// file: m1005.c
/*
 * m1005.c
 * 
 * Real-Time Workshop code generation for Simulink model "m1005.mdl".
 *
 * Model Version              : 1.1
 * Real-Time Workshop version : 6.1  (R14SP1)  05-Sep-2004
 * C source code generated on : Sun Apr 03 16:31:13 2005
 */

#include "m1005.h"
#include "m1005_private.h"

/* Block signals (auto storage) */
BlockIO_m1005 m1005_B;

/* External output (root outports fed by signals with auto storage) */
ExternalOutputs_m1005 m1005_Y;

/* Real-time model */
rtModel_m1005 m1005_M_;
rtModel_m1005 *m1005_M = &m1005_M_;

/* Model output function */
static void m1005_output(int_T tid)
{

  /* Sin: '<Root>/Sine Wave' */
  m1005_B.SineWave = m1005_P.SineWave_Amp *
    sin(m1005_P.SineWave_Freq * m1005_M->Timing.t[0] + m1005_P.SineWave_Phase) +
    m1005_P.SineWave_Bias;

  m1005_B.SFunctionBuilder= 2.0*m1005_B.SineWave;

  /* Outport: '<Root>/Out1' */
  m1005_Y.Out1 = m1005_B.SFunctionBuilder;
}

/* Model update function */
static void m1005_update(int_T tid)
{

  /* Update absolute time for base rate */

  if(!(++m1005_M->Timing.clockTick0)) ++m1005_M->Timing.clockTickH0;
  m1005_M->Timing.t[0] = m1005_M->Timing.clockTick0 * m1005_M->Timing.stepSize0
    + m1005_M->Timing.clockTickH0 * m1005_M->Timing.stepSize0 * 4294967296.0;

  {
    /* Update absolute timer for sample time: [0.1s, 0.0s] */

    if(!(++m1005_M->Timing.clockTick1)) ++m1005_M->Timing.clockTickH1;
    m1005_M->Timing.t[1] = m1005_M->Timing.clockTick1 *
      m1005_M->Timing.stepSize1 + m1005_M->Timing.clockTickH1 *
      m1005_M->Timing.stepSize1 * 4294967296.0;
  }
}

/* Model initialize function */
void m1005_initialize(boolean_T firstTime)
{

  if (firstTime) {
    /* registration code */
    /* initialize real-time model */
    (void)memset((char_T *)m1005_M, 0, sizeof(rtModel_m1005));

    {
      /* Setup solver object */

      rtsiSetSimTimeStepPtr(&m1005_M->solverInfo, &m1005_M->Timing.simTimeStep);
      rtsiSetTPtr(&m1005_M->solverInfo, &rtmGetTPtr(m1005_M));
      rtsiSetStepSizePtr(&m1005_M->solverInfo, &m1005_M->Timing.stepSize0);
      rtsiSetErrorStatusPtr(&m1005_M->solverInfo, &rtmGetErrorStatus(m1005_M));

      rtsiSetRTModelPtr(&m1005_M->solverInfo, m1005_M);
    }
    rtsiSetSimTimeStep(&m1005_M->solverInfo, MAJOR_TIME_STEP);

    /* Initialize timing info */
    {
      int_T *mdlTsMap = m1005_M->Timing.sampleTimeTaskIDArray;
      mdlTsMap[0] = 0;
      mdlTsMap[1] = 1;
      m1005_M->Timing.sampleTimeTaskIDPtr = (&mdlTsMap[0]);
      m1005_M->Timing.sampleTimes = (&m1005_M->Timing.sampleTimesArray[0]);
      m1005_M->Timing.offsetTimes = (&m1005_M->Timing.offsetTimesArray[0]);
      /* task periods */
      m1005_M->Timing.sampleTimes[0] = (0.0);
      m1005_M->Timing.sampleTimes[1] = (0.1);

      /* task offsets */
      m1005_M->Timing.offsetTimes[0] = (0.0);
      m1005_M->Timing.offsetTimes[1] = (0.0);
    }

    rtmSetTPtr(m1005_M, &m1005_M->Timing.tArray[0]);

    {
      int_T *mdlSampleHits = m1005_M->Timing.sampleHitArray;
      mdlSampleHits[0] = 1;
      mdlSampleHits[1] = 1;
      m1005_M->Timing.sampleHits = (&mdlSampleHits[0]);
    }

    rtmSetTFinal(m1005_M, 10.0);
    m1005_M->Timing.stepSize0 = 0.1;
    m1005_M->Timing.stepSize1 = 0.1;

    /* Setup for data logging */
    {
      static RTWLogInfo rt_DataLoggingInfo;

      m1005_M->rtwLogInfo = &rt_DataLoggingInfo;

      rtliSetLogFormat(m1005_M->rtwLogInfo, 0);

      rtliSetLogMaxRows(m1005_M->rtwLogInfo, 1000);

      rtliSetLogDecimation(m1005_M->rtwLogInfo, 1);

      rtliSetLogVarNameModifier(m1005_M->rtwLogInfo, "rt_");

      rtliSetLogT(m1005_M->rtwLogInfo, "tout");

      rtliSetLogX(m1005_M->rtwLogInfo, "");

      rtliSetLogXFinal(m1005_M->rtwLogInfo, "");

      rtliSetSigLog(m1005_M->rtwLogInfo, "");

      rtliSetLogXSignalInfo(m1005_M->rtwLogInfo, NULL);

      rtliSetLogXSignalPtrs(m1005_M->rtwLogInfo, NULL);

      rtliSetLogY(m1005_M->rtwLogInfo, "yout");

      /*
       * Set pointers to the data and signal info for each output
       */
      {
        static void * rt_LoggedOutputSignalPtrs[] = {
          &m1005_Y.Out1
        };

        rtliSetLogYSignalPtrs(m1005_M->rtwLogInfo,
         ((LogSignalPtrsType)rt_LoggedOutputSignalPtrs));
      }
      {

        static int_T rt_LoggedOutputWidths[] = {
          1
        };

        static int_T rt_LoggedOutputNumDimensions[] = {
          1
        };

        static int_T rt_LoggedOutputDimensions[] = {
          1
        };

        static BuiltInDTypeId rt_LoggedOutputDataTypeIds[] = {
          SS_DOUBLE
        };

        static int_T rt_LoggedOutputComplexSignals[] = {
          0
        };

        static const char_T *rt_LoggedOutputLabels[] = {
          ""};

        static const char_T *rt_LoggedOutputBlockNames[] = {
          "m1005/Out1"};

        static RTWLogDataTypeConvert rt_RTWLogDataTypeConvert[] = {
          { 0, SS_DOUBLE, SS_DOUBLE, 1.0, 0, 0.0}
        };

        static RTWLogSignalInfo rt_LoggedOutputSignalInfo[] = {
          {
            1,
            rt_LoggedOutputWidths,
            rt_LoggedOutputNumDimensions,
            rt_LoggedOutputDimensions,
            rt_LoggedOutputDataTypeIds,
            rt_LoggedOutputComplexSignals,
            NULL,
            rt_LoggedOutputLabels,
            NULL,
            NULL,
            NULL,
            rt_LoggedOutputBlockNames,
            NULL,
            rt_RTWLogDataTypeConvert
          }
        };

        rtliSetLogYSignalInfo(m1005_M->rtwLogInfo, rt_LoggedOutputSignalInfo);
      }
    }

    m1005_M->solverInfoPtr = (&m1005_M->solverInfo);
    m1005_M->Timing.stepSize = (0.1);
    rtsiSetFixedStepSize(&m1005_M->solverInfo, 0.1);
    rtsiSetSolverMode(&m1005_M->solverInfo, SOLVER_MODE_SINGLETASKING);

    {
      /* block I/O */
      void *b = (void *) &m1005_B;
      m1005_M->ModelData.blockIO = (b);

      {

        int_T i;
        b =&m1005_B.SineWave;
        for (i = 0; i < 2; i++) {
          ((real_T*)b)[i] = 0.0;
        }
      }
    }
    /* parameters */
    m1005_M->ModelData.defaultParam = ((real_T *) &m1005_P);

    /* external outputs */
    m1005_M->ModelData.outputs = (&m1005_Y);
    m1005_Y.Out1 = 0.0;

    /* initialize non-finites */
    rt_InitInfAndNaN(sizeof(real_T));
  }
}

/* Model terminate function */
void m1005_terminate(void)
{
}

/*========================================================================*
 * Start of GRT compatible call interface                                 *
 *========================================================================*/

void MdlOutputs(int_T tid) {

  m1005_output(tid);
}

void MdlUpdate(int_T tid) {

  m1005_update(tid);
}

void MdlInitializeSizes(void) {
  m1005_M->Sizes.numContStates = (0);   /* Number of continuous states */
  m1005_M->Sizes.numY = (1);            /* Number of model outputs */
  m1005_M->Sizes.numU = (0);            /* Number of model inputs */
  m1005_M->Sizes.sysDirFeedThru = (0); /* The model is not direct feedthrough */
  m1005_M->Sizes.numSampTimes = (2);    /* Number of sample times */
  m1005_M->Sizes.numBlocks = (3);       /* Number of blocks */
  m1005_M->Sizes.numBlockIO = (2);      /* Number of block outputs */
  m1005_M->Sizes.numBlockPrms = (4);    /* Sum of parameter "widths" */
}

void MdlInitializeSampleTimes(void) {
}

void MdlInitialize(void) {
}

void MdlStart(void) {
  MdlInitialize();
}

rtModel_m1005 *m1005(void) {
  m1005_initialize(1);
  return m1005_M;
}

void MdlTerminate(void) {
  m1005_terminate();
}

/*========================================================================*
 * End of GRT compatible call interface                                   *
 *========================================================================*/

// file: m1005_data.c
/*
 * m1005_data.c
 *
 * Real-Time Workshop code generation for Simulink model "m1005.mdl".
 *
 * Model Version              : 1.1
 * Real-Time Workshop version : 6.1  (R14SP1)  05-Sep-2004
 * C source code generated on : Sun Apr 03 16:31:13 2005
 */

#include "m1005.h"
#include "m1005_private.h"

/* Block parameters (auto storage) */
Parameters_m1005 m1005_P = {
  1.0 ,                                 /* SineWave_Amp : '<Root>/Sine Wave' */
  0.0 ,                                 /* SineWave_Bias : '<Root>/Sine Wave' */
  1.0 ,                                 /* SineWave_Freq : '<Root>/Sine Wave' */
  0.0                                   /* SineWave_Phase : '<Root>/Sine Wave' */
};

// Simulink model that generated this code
simulink model "m1005"  (Simulink 6.1)
settings: Solver=FixedStepDiscrete  StartTime=0.0  StopTime=10.0  FixedStep=0.1  RelTol=1e-3

== system m1005 ==
  S-Function Builder : S-Function  FunctionName=myfunc  SFunctionModules=myfunc_wrapper  WizardData=DataTag0  mask(S-Function Builder){}
      mask init:
      | val = [[.9  0.75 0.75 1 1 .9 .9 1]',[1 1 0.75 0.75 .9 .9 1 .9]'];try , sys = get_param(gcb,'SfunBuilderFcnName');if isempty(sys), sys = get_param(gcb,'FunctionName'); end,catch, sys = get_param(gcb,'FunctionName'); end
  Sine Wave : Sin  SampleTime=0
  Out1 : Outport
  wires:
  Sine Wave/1 -> S-Function Builder/1
  S-Function Builder/1 -> Out1/1
